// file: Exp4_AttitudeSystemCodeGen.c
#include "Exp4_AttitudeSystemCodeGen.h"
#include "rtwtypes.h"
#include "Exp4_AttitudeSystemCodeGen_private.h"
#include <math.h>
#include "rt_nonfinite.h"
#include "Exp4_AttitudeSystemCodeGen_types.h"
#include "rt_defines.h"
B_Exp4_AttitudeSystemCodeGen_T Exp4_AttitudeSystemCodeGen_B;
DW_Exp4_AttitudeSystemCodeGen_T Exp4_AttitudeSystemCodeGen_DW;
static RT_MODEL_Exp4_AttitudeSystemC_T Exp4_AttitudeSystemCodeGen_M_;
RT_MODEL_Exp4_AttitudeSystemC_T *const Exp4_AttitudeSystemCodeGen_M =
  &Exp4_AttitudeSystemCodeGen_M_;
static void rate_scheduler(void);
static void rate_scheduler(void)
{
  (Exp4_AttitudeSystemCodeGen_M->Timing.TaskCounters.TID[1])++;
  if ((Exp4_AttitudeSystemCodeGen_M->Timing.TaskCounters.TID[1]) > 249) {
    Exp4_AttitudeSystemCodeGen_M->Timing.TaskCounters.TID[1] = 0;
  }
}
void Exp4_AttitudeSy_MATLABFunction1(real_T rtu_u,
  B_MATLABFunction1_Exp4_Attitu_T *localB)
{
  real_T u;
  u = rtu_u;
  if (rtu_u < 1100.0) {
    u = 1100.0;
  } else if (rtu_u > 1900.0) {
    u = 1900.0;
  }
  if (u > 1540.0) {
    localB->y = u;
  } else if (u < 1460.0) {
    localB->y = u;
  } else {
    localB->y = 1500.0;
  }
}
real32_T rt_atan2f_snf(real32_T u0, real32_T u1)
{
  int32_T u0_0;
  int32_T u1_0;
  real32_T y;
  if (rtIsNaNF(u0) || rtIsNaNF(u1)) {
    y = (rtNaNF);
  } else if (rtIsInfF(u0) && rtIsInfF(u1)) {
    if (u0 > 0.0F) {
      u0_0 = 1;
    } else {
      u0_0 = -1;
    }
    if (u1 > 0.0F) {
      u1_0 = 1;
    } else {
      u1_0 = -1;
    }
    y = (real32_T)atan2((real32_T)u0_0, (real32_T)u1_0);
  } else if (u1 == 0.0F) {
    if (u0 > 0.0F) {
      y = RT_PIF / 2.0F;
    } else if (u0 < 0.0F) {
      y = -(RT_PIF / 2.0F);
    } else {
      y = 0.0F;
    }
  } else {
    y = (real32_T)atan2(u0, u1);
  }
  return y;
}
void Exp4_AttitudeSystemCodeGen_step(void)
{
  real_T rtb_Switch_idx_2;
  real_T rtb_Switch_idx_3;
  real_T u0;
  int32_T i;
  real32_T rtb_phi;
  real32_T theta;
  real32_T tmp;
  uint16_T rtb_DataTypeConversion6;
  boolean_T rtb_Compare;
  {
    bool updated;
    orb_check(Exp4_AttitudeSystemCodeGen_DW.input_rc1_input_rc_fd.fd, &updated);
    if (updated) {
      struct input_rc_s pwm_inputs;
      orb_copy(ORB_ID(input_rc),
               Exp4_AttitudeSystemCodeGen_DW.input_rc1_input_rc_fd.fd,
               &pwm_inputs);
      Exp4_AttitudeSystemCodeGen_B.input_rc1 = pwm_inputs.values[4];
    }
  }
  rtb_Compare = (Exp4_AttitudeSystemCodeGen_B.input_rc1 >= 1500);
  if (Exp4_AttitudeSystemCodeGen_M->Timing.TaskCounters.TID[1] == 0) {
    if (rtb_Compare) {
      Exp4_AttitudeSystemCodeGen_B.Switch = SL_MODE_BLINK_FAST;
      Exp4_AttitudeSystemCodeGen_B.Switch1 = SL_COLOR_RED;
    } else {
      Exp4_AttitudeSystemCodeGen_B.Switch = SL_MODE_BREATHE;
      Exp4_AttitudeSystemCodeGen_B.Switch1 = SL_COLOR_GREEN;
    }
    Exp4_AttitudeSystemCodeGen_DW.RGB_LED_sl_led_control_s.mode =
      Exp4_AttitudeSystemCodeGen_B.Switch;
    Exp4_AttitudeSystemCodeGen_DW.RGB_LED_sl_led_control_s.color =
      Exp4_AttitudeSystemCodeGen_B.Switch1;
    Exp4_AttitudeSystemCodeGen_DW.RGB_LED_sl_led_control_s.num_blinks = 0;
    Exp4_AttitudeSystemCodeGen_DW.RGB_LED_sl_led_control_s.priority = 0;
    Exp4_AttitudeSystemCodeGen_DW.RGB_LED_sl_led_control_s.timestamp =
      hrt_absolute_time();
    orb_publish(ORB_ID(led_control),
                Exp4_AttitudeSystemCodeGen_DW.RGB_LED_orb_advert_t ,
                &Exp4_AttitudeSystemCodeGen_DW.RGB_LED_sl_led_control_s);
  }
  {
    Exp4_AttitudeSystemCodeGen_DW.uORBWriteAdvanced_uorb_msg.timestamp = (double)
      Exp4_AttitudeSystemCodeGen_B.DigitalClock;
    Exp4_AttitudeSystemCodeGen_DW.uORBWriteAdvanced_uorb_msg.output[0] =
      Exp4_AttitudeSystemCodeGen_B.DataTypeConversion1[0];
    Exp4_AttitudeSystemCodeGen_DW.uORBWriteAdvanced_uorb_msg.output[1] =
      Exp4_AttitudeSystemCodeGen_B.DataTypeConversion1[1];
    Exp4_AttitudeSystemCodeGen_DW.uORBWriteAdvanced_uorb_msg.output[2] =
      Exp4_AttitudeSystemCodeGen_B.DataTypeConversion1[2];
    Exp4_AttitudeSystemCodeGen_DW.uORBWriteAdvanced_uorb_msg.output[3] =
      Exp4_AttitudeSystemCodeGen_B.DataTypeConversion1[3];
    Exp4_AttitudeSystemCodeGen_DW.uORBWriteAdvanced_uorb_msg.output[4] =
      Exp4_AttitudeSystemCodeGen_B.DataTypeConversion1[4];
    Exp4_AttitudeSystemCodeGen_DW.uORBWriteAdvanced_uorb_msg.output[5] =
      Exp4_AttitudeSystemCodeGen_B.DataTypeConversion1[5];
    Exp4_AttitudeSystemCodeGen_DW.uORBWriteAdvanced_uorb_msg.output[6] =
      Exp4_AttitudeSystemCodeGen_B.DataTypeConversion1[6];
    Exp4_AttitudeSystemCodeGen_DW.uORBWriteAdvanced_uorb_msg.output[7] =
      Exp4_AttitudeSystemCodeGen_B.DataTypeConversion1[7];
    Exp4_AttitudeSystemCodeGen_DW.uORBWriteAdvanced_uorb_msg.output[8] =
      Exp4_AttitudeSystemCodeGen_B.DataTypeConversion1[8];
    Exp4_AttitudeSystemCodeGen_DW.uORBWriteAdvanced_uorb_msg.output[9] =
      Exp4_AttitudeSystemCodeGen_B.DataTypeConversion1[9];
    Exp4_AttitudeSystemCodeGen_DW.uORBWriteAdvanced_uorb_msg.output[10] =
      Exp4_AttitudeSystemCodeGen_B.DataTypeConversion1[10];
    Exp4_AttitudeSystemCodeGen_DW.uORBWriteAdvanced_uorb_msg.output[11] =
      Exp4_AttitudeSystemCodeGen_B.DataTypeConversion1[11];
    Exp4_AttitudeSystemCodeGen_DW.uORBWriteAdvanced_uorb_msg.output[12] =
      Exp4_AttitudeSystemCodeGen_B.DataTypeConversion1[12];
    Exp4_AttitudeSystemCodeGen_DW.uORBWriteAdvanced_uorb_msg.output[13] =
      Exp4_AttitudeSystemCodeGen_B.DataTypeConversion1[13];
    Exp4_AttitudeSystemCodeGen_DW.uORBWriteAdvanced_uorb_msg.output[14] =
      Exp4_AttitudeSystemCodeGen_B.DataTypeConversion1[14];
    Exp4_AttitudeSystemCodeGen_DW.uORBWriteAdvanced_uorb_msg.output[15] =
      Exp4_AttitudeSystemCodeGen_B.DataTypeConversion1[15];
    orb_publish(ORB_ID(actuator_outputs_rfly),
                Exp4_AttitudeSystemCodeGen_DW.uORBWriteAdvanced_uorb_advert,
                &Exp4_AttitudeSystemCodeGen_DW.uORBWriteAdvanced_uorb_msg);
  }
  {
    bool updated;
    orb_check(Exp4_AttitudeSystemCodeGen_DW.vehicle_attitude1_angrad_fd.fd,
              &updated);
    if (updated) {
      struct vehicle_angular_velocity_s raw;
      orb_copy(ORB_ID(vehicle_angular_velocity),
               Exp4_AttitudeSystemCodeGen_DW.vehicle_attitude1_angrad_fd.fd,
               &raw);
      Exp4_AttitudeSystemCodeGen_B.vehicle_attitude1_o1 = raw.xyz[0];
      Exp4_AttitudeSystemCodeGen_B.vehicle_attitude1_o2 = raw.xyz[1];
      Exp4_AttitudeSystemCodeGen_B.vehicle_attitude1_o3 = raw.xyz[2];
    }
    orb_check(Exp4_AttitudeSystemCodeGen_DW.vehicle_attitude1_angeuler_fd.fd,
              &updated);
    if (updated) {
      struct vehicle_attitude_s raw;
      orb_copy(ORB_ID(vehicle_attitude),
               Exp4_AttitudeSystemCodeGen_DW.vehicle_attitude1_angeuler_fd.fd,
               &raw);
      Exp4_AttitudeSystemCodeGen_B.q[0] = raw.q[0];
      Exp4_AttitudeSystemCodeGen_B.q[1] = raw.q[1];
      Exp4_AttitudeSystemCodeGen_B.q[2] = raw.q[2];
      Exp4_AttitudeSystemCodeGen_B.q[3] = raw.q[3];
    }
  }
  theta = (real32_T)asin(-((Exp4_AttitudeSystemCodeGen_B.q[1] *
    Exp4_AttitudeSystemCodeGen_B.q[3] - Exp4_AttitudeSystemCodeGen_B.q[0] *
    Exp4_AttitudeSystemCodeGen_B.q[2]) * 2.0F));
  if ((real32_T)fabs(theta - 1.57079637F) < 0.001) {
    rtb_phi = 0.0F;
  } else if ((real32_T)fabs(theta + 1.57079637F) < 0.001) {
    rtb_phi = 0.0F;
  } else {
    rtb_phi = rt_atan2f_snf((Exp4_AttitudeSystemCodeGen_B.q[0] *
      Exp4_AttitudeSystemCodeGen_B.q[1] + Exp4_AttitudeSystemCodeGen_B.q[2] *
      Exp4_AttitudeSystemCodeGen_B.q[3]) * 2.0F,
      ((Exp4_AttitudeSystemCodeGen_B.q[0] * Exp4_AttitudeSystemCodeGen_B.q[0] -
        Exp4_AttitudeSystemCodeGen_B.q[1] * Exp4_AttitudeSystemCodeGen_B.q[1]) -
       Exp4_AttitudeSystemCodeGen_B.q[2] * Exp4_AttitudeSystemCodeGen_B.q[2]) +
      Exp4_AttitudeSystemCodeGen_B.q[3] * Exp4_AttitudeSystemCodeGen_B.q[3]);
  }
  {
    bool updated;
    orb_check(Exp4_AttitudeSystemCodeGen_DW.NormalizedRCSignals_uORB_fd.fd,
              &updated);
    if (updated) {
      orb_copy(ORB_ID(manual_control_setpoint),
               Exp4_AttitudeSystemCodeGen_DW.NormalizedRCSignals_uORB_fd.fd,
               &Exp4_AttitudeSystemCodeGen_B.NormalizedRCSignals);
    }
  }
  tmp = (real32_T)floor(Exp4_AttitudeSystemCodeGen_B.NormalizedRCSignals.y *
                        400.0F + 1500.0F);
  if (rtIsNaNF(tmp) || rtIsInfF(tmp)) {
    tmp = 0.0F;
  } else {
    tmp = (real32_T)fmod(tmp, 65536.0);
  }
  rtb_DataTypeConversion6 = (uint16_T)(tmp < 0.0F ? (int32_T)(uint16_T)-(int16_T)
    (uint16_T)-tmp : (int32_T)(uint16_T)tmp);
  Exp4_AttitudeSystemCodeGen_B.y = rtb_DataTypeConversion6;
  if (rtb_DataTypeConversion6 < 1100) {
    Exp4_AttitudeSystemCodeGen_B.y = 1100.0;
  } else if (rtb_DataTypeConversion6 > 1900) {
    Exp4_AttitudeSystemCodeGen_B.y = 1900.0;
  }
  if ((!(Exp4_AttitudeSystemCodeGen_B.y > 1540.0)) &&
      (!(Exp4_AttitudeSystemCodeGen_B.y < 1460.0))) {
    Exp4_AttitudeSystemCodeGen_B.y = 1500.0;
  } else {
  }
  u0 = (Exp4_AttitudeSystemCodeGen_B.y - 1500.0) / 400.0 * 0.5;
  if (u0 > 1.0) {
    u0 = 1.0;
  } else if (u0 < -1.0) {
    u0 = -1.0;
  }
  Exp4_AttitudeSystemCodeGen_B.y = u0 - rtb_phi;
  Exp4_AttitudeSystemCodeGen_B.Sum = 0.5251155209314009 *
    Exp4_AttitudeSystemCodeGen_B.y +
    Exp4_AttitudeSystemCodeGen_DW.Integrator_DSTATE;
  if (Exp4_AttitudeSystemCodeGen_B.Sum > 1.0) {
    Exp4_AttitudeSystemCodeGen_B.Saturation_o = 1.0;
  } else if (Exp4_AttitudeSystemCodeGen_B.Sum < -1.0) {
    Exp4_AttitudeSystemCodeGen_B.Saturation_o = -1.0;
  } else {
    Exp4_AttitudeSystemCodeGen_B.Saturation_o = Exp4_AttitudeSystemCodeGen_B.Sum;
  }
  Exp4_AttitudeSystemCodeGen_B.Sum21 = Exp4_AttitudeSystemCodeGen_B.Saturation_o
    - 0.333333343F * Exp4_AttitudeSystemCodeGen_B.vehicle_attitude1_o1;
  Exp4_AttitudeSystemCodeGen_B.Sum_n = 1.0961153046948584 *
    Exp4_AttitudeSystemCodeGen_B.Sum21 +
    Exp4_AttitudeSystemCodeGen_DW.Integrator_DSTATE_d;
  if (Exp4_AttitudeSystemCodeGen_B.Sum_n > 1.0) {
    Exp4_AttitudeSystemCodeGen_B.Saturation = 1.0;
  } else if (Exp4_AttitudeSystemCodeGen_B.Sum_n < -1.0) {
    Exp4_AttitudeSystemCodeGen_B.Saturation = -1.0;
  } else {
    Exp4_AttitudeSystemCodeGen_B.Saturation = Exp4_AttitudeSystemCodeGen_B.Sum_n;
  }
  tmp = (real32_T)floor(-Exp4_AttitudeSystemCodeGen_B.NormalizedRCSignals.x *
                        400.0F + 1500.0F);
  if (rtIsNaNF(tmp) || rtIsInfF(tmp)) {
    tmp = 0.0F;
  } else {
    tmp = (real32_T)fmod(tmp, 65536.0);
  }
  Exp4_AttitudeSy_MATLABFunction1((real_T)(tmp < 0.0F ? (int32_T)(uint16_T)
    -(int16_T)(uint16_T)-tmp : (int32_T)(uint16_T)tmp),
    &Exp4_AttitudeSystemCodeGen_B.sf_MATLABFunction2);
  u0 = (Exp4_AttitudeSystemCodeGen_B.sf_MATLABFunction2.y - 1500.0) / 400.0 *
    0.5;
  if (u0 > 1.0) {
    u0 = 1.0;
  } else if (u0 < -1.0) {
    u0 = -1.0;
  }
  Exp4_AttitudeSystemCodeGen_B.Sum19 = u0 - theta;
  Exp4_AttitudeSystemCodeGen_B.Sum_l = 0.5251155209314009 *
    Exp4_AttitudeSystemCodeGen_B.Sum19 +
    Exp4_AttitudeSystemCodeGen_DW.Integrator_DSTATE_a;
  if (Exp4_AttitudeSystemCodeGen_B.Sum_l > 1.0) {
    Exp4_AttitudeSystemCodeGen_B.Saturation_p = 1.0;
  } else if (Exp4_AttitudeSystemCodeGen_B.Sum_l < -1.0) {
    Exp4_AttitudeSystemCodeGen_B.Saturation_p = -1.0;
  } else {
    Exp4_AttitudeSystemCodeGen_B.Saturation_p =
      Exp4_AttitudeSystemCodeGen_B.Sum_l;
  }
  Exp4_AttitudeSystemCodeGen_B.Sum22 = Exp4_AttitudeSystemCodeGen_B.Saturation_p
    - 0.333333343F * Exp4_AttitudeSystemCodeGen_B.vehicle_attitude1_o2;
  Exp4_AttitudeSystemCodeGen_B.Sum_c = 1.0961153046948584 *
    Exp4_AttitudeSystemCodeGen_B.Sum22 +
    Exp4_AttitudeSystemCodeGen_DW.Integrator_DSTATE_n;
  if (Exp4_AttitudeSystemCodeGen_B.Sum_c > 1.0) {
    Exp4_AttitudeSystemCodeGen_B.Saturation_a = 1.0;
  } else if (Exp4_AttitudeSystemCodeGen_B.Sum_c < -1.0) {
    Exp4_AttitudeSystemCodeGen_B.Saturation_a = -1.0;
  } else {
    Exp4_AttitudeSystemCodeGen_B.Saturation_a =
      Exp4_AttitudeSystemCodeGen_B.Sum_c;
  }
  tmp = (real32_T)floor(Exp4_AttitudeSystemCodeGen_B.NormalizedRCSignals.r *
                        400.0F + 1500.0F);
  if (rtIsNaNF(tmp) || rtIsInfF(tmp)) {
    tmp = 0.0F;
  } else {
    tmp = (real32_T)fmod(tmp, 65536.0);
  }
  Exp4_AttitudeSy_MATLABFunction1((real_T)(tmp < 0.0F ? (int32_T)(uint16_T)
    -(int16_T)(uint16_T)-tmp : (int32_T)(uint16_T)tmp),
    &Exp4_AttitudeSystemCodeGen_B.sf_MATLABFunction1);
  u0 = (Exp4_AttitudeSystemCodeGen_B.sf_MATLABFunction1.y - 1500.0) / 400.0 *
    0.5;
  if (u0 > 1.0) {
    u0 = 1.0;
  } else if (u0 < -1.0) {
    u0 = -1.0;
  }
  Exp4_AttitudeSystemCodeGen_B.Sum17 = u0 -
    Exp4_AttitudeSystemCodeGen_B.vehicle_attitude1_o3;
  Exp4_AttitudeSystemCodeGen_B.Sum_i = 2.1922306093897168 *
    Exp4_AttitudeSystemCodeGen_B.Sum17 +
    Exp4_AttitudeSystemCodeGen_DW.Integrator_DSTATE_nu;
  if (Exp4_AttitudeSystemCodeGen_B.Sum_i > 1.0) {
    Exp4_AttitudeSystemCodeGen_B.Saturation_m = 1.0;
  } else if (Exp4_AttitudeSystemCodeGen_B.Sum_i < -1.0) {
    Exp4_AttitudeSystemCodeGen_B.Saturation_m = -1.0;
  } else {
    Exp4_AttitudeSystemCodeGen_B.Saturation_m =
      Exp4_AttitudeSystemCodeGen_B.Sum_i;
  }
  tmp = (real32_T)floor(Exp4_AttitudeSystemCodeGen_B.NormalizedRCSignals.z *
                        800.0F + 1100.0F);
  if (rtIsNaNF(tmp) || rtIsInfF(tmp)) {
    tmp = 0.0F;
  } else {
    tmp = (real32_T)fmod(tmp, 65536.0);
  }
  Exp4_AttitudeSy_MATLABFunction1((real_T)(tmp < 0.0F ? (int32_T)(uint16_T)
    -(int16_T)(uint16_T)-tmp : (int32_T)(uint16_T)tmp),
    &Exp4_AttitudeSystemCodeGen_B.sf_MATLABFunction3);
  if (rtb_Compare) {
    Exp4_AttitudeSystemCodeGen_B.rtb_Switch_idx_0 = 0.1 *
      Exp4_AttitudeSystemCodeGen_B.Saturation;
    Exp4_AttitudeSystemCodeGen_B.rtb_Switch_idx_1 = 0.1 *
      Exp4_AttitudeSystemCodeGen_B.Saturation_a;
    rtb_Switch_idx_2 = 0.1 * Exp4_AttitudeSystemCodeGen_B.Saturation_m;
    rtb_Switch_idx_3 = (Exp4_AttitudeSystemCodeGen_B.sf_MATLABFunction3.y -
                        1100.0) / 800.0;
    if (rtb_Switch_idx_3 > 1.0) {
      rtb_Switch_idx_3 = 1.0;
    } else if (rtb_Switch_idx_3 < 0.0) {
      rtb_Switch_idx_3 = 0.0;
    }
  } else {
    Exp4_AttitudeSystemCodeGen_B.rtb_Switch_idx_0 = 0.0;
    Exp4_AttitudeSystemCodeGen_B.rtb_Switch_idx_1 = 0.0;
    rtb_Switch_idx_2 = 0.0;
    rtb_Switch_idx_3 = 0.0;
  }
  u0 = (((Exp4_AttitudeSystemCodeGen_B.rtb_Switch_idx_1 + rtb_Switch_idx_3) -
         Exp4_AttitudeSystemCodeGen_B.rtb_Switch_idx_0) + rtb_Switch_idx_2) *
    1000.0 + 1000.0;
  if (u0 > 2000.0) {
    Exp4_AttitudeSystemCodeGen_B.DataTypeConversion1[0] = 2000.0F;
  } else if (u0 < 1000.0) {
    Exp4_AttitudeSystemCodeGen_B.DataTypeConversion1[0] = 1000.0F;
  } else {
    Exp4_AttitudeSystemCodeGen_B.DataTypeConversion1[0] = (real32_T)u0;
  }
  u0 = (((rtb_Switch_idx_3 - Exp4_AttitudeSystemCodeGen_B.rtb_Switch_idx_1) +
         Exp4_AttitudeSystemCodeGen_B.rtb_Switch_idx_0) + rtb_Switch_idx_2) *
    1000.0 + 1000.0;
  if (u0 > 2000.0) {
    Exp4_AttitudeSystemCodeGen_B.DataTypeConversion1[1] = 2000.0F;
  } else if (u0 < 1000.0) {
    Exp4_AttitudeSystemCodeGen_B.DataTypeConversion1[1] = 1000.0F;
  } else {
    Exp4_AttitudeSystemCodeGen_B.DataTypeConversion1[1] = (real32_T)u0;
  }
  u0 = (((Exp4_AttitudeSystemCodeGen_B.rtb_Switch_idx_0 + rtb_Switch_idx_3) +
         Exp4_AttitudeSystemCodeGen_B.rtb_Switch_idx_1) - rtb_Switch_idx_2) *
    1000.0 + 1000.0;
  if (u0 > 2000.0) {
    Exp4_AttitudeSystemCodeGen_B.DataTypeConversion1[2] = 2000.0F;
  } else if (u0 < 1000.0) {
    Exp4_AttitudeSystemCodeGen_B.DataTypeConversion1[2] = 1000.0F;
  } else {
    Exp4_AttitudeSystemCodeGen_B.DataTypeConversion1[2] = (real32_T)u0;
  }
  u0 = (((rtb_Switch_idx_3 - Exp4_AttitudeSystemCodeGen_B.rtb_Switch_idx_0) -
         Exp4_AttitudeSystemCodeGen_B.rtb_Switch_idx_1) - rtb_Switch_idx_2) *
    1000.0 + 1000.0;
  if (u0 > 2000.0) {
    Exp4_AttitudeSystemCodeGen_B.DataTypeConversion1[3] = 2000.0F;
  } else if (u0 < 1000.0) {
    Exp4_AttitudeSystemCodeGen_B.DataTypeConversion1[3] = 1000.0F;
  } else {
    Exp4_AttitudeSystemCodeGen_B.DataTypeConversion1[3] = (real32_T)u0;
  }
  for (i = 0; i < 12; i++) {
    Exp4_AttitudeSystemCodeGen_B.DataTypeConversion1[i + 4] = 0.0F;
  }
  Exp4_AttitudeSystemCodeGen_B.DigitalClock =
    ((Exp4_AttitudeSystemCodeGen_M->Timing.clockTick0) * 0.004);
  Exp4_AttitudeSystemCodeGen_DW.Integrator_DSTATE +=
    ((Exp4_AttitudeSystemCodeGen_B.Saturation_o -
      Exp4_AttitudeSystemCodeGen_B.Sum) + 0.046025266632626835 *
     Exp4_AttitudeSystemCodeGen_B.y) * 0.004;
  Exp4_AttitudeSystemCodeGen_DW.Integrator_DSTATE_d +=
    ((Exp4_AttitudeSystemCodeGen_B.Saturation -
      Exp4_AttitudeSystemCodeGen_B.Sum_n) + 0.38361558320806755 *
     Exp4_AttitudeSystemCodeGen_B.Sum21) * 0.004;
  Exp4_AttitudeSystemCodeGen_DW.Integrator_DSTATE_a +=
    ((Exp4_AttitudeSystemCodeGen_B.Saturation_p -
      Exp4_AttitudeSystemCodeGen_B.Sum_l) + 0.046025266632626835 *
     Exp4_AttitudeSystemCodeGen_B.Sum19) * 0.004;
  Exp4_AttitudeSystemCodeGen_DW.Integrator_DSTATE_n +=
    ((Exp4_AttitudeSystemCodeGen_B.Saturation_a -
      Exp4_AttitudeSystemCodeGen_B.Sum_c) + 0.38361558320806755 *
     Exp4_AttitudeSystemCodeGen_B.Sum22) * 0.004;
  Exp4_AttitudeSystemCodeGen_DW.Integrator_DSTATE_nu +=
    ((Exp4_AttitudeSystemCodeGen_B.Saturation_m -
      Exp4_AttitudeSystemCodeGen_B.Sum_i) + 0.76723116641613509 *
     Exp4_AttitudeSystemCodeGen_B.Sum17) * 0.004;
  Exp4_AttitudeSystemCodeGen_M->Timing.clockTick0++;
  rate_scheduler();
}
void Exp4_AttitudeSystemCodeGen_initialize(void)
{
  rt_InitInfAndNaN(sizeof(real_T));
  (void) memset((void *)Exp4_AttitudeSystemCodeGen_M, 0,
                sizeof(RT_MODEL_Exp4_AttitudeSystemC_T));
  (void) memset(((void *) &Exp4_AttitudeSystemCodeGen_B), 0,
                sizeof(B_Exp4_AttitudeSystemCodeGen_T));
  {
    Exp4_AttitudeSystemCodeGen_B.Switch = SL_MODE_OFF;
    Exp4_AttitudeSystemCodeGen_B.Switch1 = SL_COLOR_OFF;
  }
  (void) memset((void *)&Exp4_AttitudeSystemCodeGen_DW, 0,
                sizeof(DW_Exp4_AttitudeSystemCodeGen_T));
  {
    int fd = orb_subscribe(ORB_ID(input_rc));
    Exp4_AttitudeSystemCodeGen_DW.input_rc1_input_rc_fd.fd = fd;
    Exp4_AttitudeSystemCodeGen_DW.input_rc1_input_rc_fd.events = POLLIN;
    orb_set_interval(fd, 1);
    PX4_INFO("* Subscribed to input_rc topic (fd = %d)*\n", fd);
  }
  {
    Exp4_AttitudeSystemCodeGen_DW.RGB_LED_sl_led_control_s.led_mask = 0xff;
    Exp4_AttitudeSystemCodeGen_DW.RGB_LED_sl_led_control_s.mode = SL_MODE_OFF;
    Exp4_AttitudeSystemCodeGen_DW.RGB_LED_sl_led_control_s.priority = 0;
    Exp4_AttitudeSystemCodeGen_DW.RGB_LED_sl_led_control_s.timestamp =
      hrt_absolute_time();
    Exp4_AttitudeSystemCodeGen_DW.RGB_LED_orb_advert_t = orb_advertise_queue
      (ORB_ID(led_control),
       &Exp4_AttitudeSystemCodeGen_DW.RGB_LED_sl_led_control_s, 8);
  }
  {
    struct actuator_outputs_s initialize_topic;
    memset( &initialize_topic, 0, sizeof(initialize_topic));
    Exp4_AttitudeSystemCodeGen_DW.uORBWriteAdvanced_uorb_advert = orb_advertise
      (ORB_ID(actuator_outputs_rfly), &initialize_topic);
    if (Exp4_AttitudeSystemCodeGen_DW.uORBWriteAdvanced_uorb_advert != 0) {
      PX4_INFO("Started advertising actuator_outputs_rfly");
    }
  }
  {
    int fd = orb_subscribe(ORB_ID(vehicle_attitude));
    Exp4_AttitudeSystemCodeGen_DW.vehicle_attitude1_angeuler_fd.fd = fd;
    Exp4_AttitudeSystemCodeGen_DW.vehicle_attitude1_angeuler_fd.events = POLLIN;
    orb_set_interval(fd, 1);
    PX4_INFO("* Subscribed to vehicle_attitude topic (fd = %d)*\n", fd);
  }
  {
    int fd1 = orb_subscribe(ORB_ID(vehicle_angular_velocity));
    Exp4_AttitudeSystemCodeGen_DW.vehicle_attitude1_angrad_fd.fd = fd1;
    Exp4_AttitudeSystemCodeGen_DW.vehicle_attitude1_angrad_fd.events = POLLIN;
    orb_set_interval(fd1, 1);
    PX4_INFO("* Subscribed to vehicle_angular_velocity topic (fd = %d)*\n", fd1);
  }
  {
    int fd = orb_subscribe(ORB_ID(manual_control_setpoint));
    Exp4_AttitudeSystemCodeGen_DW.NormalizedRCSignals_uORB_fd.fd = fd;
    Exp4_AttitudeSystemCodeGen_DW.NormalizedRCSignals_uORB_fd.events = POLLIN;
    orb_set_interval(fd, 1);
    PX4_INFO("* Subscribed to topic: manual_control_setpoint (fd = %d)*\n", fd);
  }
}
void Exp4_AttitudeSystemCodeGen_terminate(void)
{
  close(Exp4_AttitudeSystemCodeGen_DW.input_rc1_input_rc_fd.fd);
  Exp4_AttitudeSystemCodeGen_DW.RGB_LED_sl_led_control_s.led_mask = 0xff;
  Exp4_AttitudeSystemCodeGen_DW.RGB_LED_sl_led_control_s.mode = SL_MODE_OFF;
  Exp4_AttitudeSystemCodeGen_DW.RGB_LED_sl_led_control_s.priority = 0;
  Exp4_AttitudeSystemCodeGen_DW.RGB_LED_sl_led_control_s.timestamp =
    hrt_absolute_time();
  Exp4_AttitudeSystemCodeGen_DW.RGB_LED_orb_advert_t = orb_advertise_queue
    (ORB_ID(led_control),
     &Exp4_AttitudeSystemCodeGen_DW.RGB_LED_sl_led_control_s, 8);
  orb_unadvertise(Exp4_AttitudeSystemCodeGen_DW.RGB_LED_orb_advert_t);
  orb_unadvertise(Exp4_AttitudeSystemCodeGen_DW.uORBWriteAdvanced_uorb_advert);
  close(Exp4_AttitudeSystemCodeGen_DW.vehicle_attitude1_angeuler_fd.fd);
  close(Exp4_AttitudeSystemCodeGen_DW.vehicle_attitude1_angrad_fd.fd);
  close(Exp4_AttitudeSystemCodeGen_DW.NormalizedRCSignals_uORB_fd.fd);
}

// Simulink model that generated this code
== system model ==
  RGB_LED : pixhawk_slib_sensors_actuators/RGB_LED  <- 1: Switch, 2: Switch1
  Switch : Switch  Criteria=u2 ~= 0  Threshold=1500  <- 1: Constant#1, 2: RateTransition#1, 3: Constant#2
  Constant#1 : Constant  Value=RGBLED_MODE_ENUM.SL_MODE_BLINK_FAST
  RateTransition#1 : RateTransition  <- 1: CompareToConstant#1
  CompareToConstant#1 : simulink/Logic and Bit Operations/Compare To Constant  relop=>=  const=uint16(1500)  <- 1: DataTypeConversion#1
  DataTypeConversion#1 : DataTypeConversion  <- 1: input_rc1
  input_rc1 : pixhawk_slib_sensors_actuators/input_rc
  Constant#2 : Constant  Value=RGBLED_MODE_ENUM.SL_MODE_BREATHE
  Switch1 : Switch  Criteria=u2 ~= 0  Threshold=1500  <- 1: Constant#3, 2: RateTransition#1, 3: Constant#4
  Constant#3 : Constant  Value=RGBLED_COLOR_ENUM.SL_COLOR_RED
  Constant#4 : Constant  Value=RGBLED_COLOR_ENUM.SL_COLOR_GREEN
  uORBWriteAdvanced : pixhawk_slib_uORB_RW/uORB Write Advanced  <- 1: DigitalClock, 2: DataTypeConversion1
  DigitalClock : DigitalClock
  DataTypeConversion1 : DataTypeConversion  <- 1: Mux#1
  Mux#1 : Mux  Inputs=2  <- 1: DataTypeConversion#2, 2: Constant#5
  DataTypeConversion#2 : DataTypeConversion  <- 1: Saturate#1
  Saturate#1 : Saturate  UpperLimit=2000  LowerLimit=1000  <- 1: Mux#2
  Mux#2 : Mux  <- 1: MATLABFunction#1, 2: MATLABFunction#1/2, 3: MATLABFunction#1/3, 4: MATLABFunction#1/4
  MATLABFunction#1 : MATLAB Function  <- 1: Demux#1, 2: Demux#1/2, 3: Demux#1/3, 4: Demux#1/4
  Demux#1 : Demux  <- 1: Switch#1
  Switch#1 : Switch  Criteria=u2 > Threshold  Threshold=0.5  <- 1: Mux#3, 2: CompareToConstant#1, 3: Constant#6
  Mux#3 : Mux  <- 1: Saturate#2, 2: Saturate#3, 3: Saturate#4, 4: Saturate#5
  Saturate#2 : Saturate  UpperLimit=1  LowerLimit=-1  <- 1: Gain#1
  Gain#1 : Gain  Gain=1/10  <- 1: PIDController#1
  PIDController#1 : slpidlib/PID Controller  Controller=PI  Form=Parallel  TimeDomain=Discrete-time  IntegratorMethod=Forward Euler  P=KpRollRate  I=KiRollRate  D=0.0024  N=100  InitialConditionForIntegrator=0  ExternalReset=none  LimitOutput=on  UpperSaturationLimit=1  LowerSaturationLimit=-1  <- 1: Sum21
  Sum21 : Sum  Inputs=-+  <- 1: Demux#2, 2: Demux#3
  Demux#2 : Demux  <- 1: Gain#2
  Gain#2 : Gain  Gain=1/3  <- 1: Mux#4
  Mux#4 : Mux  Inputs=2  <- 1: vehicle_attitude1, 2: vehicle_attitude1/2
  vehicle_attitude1 : pixhawk_slib_sensors_actuators/vehicle_attitude
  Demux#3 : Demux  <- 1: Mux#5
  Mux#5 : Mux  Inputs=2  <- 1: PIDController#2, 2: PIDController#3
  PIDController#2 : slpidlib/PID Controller  Controller=PI  Form=Parallel  TimeDomain=Discrete-time  IntegratorMethod=Forward Euler  P=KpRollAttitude  I=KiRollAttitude  D=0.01  N=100  InitialConditionForIntegrator=0  ExternalReset=none  LimitOutput=on  UpperSaturationLimit=1  LowerSaturationLimit=-1  <- 1: Sum#1
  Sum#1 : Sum  Inputs=-+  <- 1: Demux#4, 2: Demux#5
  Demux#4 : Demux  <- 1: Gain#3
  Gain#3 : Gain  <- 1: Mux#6
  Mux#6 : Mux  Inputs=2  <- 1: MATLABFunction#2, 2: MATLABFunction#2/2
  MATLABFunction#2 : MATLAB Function  <- 1: vehicle_attitude1/4
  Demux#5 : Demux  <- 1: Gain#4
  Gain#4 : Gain  Gain=[1 1]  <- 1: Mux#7
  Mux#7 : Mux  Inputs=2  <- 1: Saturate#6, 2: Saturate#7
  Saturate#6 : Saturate  UpperLimit=1  LowerLimit=-1  <- 1: Gain#5
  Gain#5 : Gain  Gain=0.5  <- 1: Fcn#1
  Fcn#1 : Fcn  Expr=(u - 1500)/400  <- 1: MATLABFunction#3
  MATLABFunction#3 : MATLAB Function  <- 1: DataTypeConversion#3
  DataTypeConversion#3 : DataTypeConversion  <- 1: DataTypeConversion#4
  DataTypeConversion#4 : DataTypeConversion  <- 1: Fcn#2
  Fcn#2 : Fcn  Expr=u*400+1500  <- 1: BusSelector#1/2
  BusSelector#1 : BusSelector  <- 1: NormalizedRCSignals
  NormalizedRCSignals : pixhawk_slib_uORB_RW/uORB Read Function-Call Trigger
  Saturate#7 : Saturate  UpperLimit=1  LowerLimit=-1  <- 1: Gain#6
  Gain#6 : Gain  Gain=0.5  <- 1: Fcn#3
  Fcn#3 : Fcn  Expr=(u - 1500)/400  <- 1: MATLABFunction2
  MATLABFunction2 : MATLAB Function  <- 1: DataTypeConversion#5
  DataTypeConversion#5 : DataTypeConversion  <- 1: DataTypeConversion#6
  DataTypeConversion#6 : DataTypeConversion  <- 1: Fcn#4
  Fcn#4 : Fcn  Expr=u*400+1500  <- 1: Gain#7
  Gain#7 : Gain  Gain=-1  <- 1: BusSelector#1
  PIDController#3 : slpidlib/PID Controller  Controller=PI  Form=Parallel  TimeDomain=Discrete-time  IntegratorMethod=Forward Euler  P=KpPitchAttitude  I=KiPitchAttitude  D=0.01  N=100  InitialConditionForIntegrator=0  ExternalReset=none  LimitOutput=on  UpperSaturationLimit=1  LowerSaturationLimit=-1  <- 1: Sum19
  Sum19 : Sum  Inputs=-+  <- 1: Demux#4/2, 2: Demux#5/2
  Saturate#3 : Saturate  UpperLimit=1  LowerLimit=-1  <- 1: Gain#8
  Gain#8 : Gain  Gain=1/10  <- 1: PIDController#4
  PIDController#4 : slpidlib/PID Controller  Controller=PI  Form=Parallel  TimeDomain=Discrete-time  IntegratorMethod=Forward Euler  P=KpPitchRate  I=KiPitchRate  D=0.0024  N=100  InitialConditionForIntegrator=0  ExternalReset=none  LimitOutput=on  UpperSaturationLimit=1  LowerSaturationLimit=-1  <- 1: Sum22
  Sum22 : Sum  Inputs=-+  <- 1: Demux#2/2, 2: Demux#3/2
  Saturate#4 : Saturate  UpperLimit=1  LowerLimit=-1  <- 1: Gain#9
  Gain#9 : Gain  Gain=1/10  <- 1: PIDController#5
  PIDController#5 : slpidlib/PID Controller  Controller=PI  Form=Parallel  TimeDomain=Discrete-time  IntegratorMethod=Forward Euler  P=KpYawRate  I=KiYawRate  D=0  N=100  InitialConditionForIntegrator=0  ExternalReset=none  LimitOutput=on  UpperSaturationLimit=1  LowerSaturationLimit=-1  <- 1: Sum17
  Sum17 : Sum  Inputs=-+  <- 1: Gain#10, 2: Gain#11
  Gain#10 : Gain  <- 1: vehicle_attitude1/3
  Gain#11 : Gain  <- 1: Saturate#8
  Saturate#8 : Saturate  UpperLimit=1  LowerLimit=-1  <- 1: Gain#12
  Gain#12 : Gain  Gain=0.5  <- 1: Fcn#5
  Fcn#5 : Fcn  Expr=(u - 1500)/400  <- 1: MATLABFunction1
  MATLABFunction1 : MATLAB Function  <- 1: DataTypeConversion#7
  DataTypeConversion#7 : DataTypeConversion  <- 1: DataTypeConversion#8
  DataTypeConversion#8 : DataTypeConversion  <- 1: Fcn#6
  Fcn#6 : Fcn  Expr=u*400+1500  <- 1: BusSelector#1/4
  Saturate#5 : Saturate  UpperLimit=1  LowerLimit=0  <- 1: Saturate#9
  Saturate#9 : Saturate  UpperLimit=1  LowerLimit=0  <- 1: Fcn#7
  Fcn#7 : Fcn  Expr=(u - 1100) / 800  <- 1: MATLABFunction3
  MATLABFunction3 : MATLAB Function  <- 1: DataTypeConversion#9
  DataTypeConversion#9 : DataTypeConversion  <- 1: DataTypeConversion6
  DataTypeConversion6 : DataTypeConversion  <- 1: Fcn#8
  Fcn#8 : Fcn  Expr=u*800+1100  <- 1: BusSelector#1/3
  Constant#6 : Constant  Value=[0,0,0,0]
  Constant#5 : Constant  Value=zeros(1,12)
== matlab function MATLABFunction#1 ==
function [M1, M2, M3, M4] = motor_mixer(Roll, Pitch, Yaw, Thrust)

idle_PWM = 1000;

% Quad XROLL （根据QP里面的叉字形结构的文字）
% M1 = ((Pitch+ Yaw)+Thrust-Roll) * 1000 + idle_PWM;
 %M2 = ((Pitch - Yaw)+Thrust+Roll) * 1000 + idle_PWM;
 %M3 = ((Roll +Yaw) + Thrust-Pitch) * 1000 + idle_PWM;
 %M4 = ((-Roll - Pitch-Yaw) + Thrust) * 1000 + idle_PWM;
% M5 = 1000;
% M6 = 1000;
% M7 = 1000;
% M8 = 1000;
%qp上实际的输出
M1 = (Thrust+Pitch-Roll+Yaw) * 1000 + idle_PWM;
 M2 = (Thrust-Pitch +Roll+Yaw) * 1000 + idle_PWM;
 M3 = ( Thrust+Roll+Pitch-Yaw) * 1000 + idle_PWM;
 M4 = (Thrust-Roll- Pitch -Yaw) * 1000 + idle_PWM;
% Quad +
 %M1 = ((Pitch - Yaw) * Thrust / 2 + Thrust) * 1000 + idle_PWM;
 %M2 = ((-Roll + Yaw) * Thrust / 2 + Thrust) * 1000 + idle_PWM;
% M3 = ((-Pitch - Yaw) * Thrust / 2 + Thrust) * 1000 + idle_PWM;
 %M4 = ((Roll + Yaw) * Thrust / 2 + Thrust) * 1000 + idle_PWM;
% M5 = 1000;
% M6 = 1000;
% M7 = 1000;
% M8 = 1000;

% Hex X
% M1 = ((Pitch + Roll / 2 - Yaw) * Thrust / 2 + Thrust) * 1000 + idle_PWM;
% M2 = ((Pitch - Roll / 2 + Yaw) * Thrust / 2 + Thrust) * 1000 + idle_PWM;
% M3 = ((-Roll - Yaw) * Thrust / 2 + Thrust) * 1000 + idle_PWM;
% M4 = ((-Pitch - Roll / 2 + Yaw) * Thrust / 2 + Thrust) * 1000 + idle_PWM;
% M5 = ((-Pitch + Roll / 2 - Yaw) * Thrust / 2 + Thrust) * 1000 + idle_PWM;
% M6 = ((Roll + Yaw) * Thrust / 2 + Thrust) * 1000 + idle_PWM;
% M7 = 1000;
% M8 = 1000;

% Hex X (From Adam)
%M1 = uint16(single(((-Roll - Yaw) * Thrust / 3 + Thrust) * single(1000))) + idle_PWM;
%M2 = uint16(single(((Roll + Yaw) * Thrust / 3 + Thrust) * single(1000))) + idle_PWM;
%M3 = uint16(single(((Pitch + (Roll / 2) - Yaw) * Thrust / 3 + Thrust) * single(1000))) + idle_PWM;
%M4 = uint16(single(((-Pitch - (Roll / 2) + Yaw) * Thrust / 3 + Thrust) * single(1000))) + idle_PWM;
%M5 = uint16(single(((Pitch - (Roll / 2) + Yaw) * Thrust / 3 + Thrust) * single(1000))) + idle_PWM;
%M6 = uint16(single(((-Pitch + (Roll / 2) - Yaw) * Thrust / 3 + Thrust) * single(1000))) + idle_PWM;

% Hex X (Version 2)
% Roll/Yaw
% M1 = ((-Roll - Yaw) * Thrust / 2 + Thrust) * 1000 + idle_PWM;
% M2 = ((Roll + Yaw) * Thrust / 2 + Thrust) * 1000 + idle_PWM;
% % + Pitch/Roll
% M6 = ((Pitch + Roll / 2 - Yaw) * Thrust / 2 + Thrust) * 1000 + idle_PWM;
% M4 = ((Pitch - Roll / 2 + Yaw) * Thrust / 2 + Thrust) * 1000 + idle_PWM;
% % - Pitch/Roll
% M5 = ((-Pitch - Roll / 2 + Yaw) * Thrust / 2 + Thrust) * 1000 + idle_PWM;
% M3 = ((-Pitch + Roll / 2 - Yaw) * Thrust / 2 + Thrust) * 1000 + idle_PWM;

== matlab function MATLABFunction#3 ==
function y = fcn(u)
%将遥控输入的范围控制在1100~1900，同时设置一个死区，死区大小为±deadZone
RCMin = 1100;
RCMax = 1900;
deadZoneRate = 0.05;
deadZone = deadZoneRate*(RCMax-RCMin);
%限幅
if(u < RCMin)
    u = RCMin;
elseif(u > RCMax)
    u = RCMax;
end
%死区
 if(u > 1500+deadZone)
    y = u;
 elseif(u < 1500-deadZone)
     y = u;
 else
     y = 1500;
 end
     
 end

== matlab function MATLABFunction1 ==
function y = fcn(u)
%将遥控输入的范围控制在1100~1900，同时设置一个死区，死区大小为±deadZone
RCMin = 1100;
RCMax = 1900;
deadZoneRate = 0.05;
deadZone = deadZoneRate*(RCMax-RCMin);
%限幅
if(u < RCMin)
    u = RCMin;
elseif(u > RCMax)
    u = RCMax;
end
%死区
 if(u > 1500+deadZone)
    y = u;
 elseif(u < 1500-deadZone)
     y = u;
 else
     y = 1500;
 end
     
 end

== matlab function MATLABFunction2 ==
function y = fcn(u)
%将遥控输入的范围控制在1100~1900，同时设置一个死区，死区大小为±deadZone
RCMin = 1100;
RCMax = 1900;
deadZoneRate = 0.05;
deadZone = deadZoneRate*(RCMax-RCMin);
%限幅
if(u < RCMin)
    u = RCMin;
elseif(u > RCMax)
    u = RCMax;
end
%死区
 if(u > 1500+deadZone)
    y = u;
 elseif(u < 1500-deadZone)
     y = u;
 else
     y = 1500;
 end
     
 end

== matlab function MATLABFunction3 ==
function y = fcn(u)
%将遥控输入的范围控制在1100~1900，同时设置一个死区，死区大小为±deadZone
RCMin = 1100;
RCMax = 1900;
deadZoneRate = 0.05;
deadZone = deadZoneRate*(RCMax-RCMin);
%限幅
if(u < RCMin)
    u = RCMin;
elseif(u > RCMax)
    u = RCMax;
end
%死区
 if(u > 1500+deadZone)
    y = u;
 elseif(u < 1500-deadZone)
     y = u;
 else
     y = 1500;
 end
     
 end

== matlab function MATLABFunction#2 ==
function [phi,theta,psi] = quat2eul(q)
% Conversion from Quaternion to Euler angles based on the PX4 Firmware
% v1.6.5 release.
% 
% Quaternion -> DCM -> Euler Angles
% INPUT:
%   q: Quaternion vector of the format: (a + bi + cj + dk)
% OUTPUT:
%   [phi,theta,psi]: Euler angles in radians.
% 
 
    a = q(1);
    b = q(2);
    c = q(3);
    d = q(4);

    aSq = a*a;
    bSq = b*b;
    cSq = c*c;
    dSq = d*d;

    d_pi2 = pi/2;

    % quaternion_to_dcm
    dcm00 = aSq + bSq - cSq - dSq;
    % dcm01 = 2*(b*c - a*d);
    dcm02 = 2*(a*c + b*d);
    dcm10 = 2*(b*c + a*d);
    % dcm11 = aSq - bSq + cSq - dSq;
    dcm12 = 2*(c*d - a*b);
    dcm20 = 2*(b*d - a*c);
    dcm21 = 2*(a*b + c*d);
    dcm22 = aSq - bSq - cSq + dSq;

    % dcm_to_euler
    theta = asin(-dcm20);
    if abs(theta - d_pi2) < 1.0e-3
        phi = single(0.0);
        psi = atan2(dcm12, dcm02);
    elseif abs(theta + d_pi2) < 1.0e-3
        phi = single(0.0);
        psi = atan2(-dcm12, -dcm02);
    else
        phi = atan2(dcm21, dcm22);
        psi = atan2(dcm10, dcm00);
    end

end
